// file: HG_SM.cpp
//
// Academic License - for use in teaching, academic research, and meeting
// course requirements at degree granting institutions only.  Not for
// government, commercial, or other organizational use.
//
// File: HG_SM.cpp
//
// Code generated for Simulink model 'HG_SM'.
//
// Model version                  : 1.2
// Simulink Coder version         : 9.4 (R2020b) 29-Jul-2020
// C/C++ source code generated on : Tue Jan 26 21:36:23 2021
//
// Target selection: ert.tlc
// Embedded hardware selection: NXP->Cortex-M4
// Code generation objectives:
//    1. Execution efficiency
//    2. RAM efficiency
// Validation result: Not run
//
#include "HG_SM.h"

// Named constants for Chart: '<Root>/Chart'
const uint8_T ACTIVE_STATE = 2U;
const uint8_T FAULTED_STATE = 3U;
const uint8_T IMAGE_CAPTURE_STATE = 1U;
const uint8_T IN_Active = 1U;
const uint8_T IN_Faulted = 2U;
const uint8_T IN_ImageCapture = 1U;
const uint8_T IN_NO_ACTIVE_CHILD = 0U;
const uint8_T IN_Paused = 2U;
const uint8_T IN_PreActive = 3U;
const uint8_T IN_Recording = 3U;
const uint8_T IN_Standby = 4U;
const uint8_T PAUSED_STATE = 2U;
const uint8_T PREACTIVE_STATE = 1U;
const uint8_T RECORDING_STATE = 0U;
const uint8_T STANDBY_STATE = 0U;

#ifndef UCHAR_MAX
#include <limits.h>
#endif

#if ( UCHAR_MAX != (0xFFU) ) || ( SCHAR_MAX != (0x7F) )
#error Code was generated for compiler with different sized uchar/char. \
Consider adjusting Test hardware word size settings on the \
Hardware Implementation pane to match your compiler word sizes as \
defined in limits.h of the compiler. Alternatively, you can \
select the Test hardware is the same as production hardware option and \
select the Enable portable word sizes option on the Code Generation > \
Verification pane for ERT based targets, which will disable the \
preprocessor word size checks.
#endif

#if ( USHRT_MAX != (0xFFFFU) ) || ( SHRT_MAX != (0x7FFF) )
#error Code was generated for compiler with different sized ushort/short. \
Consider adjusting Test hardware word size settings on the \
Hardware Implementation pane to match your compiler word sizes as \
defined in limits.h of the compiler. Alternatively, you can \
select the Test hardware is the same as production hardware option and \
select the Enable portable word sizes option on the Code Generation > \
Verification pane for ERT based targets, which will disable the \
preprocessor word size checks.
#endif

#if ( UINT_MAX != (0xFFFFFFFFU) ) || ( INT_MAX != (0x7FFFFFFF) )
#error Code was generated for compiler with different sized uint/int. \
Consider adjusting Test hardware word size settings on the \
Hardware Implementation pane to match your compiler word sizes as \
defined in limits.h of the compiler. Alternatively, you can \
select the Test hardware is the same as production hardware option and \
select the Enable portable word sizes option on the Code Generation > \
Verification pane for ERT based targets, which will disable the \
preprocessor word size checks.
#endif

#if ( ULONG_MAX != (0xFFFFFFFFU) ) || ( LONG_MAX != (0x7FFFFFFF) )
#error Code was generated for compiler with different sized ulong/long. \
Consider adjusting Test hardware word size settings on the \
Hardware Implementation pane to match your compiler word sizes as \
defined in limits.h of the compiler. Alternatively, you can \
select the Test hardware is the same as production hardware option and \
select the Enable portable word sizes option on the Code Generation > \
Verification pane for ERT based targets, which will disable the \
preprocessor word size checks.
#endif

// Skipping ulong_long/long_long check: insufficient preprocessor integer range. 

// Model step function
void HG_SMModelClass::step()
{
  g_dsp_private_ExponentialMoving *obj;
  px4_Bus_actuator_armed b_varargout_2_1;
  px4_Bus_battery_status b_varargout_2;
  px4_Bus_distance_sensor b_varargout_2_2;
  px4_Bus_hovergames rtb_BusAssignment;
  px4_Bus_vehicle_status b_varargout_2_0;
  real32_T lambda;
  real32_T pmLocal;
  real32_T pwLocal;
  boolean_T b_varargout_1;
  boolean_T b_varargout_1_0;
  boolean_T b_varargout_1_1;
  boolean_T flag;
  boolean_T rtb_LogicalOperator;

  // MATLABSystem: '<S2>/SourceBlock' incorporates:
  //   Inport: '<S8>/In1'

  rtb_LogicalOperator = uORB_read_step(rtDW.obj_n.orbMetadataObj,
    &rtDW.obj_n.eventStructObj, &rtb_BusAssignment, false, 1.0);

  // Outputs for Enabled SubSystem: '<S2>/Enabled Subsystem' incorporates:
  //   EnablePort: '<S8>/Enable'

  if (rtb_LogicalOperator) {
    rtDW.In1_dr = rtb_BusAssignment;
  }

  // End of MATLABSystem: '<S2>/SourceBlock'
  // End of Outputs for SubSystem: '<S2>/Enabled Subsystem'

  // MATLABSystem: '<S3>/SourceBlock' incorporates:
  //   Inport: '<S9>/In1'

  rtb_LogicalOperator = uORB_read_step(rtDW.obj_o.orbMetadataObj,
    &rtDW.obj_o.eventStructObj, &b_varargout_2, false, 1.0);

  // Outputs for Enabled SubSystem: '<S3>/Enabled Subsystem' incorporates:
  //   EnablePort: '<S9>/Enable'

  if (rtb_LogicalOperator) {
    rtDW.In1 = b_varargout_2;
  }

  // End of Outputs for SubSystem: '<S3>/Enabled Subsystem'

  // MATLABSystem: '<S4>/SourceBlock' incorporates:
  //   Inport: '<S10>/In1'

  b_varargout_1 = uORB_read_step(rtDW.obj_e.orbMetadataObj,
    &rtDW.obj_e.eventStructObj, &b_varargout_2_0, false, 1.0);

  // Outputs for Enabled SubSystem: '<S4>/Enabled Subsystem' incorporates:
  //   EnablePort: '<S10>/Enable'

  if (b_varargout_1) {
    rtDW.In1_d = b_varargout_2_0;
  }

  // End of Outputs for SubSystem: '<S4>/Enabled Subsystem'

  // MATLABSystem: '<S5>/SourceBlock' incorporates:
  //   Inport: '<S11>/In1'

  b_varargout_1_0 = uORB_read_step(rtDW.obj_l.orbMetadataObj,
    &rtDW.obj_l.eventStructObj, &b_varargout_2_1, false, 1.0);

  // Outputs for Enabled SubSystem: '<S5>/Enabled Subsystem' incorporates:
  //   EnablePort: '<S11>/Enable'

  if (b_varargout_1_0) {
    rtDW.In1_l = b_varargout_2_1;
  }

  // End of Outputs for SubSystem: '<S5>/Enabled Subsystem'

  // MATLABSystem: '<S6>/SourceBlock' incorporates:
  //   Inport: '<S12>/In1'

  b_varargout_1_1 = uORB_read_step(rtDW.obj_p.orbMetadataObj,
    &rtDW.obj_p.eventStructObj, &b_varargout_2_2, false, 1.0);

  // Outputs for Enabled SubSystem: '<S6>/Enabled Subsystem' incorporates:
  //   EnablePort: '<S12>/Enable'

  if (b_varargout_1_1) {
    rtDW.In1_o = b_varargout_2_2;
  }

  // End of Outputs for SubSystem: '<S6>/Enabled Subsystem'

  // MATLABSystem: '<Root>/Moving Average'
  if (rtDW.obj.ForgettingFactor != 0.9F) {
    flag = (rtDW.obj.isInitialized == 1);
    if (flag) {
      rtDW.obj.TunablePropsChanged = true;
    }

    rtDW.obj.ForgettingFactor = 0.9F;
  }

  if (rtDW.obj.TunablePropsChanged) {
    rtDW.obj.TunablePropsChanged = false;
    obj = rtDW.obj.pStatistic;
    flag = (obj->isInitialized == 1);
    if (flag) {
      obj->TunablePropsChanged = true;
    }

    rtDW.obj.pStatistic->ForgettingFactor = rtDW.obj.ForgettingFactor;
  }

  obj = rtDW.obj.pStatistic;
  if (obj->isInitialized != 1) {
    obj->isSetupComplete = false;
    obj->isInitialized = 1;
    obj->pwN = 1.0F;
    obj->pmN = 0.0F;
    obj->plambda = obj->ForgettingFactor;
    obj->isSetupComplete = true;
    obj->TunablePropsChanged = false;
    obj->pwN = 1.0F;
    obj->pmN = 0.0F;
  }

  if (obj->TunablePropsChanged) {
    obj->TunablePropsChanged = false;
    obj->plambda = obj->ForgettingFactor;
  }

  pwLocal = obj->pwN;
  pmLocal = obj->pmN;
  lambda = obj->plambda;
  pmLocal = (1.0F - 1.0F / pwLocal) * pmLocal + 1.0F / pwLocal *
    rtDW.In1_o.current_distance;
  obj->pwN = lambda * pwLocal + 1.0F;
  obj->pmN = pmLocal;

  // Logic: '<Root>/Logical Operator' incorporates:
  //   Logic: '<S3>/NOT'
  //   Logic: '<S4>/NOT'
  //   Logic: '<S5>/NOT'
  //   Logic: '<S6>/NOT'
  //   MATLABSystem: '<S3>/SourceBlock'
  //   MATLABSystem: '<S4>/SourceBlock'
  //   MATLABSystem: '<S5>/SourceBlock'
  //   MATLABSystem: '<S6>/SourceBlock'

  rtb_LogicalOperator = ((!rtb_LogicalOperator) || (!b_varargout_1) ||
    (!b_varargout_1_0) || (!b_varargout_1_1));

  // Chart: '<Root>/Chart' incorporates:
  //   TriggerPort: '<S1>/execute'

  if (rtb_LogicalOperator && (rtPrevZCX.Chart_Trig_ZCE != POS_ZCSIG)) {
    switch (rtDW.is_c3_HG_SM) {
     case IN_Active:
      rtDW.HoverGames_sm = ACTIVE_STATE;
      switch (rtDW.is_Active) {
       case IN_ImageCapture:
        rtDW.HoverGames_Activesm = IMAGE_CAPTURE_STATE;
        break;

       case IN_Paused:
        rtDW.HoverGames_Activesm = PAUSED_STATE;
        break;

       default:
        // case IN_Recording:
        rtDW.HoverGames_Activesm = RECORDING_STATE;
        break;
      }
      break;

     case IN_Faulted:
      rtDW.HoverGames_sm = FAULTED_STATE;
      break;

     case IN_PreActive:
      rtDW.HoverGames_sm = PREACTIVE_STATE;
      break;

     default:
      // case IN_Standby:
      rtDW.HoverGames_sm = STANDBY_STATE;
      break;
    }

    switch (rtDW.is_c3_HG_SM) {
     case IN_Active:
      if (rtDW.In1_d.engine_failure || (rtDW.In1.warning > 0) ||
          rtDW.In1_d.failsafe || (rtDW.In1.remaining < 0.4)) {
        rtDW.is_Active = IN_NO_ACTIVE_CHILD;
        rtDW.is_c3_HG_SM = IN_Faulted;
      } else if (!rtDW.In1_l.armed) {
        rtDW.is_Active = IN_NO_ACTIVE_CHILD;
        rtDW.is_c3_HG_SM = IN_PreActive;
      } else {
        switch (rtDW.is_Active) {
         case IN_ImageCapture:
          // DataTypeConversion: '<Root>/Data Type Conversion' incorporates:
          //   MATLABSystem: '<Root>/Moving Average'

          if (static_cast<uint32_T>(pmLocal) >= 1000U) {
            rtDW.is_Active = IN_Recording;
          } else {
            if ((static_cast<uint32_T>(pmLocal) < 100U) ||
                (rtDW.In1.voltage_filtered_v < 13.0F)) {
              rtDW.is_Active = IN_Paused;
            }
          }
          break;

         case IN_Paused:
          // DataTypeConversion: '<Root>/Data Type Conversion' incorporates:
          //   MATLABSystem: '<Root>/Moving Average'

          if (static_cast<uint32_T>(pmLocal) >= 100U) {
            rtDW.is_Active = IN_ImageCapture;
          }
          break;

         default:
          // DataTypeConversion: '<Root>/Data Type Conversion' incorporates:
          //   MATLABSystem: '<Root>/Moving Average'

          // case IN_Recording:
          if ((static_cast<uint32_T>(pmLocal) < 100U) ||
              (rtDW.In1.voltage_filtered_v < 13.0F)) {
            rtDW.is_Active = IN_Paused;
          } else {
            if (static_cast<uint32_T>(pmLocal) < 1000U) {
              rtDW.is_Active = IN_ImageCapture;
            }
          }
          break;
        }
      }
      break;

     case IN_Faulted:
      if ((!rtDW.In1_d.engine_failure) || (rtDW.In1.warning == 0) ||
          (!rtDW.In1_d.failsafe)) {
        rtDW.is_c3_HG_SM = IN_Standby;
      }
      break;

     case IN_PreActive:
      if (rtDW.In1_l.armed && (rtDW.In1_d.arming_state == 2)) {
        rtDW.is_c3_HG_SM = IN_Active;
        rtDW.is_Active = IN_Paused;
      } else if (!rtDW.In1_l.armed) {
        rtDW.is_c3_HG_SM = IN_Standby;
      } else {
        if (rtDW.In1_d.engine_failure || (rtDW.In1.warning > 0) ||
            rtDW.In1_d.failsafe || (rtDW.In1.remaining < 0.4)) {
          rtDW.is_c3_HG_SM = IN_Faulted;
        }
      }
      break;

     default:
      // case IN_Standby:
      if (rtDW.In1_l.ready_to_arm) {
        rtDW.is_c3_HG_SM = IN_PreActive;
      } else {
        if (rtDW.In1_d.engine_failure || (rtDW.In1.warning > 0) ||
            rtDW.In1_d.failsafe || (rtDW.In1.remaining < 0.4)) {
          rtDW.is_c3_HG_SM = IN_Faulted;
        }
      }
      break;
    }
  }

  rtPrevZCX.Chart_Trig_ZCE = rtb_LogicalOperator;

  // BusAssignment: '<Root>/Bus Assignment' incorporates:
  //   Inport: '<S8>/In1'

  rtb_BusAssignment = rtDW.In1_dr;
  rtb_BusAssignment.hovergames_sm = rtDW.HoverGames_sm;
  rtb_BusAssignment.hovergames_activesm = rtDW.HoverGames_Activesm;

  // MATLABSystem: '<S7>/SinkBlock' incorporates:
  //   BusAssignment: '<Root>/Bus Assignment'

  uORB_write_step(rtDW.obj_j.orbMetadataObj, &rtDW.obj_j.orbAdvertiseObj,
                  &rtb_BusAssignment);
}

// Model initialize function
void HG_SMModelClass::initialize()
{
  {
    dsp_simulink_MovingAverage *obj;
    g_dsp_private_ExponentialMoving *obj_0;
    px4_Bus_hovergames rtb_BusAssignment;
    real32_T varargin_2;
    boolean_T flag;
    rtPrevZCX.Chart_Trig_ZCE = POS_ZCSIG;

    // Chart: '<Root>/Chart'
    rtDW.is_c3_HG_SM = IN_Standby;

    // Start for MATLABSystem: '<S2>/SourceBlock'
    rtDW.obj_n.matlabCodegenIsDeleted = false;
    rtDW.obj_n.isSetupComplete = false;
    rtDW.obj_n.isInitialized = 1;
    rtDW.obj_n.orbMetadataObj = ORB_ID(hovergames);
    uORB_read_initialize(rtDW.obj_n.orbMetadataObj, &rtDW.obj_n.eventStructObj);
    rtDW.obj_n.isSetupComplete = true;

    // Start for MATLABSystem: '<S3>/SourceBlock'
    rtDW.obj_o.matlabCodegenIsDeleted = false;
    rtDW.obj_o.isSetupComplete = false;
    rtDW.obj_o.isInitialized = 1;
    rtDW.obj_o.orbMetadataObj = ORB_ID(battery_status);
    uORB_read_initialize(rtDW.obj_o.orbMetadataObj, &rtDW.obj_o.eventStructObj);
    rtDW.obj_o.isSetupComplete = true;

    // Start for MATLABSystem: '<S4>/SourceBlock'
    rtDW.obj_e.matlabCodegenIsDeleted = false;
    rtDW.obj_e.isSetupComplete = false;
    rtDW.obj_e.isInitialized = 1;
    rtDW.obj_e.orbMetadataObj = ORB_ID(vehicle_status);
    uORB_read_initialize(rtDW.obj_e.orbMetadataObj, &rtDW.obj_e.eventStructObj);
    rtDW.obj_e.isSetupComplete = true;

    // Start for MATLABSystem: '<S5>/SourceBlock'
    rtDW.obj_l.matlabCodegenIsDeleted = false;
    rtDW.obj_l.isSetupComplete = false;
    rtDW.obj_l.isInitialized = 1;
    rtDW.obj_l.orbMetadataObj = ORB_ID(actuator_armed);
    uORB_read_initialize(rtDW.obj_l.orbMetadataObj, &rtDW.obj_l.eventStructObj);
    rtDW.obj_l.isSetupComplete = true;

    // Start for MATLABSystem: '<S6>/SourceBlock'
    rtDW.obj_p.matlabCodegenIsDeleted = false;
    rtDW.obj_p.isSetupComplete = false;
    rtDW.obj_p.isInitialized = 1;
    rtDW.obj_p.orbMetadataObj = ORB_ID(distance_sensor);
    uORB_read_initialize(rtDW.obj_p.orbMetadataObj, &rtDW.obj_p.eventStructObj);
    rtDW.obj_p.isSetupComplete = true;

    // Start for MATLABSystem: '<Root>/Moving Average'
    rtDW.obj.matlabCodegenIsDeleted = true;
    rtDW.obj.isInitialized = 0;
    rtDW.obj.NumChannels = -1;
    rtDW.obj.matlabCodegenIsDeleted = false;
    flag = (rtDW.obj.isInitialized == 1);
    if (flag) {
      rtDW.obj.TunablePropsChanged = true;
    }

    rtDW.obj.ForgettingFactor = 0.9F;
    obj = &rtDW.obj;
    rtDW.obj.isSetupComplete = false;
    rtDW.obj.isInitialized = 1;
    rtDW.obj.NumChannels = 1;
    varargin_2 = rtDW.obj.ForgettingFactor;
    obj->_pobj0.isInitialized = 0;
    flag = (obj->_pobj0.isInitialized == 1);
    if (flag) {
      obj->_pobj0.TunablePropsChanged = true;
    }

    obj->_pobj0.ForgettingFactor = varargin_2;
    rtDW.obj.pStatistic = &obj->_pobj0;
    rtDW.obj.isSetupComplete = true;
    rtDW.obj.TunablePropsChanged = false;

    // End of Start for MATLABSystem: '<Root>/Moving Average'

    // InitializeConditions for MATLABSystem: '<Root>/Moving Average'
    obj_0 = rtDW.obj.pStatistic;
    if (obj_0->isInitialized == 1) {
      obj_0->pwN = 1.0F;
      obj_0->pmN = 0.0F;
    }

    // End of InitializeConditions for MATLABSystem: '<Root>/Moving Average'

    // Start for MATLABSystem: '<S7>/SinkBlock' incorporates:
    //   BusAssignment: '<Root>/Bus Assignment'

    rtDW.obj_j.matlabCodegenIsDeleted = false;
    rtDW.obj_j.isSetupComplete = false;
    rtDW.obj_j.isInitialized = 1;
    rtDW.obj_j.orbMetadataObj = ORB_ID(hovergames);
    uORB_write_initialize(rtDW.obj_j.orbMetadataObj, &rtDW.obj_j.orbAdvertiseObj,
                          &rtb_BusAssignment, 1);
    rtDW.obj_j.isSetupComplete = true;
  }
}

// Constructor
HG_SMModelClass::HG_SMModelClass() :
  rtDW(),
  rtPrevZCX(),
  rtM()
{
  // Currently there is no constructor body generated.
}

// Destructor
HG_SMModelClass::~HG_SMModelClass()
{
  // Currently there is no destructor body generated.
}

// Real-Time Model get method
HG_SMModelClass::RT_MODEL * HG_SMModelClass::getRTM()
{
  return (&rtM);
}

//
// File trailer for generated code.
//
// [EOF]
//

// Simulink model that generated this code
simulink model "HG_SM"  (R2020b)
settings: Solver=FixedStepDiscrete  StartTime=0.0  StopTime=10.0  FixedStep=0.1  RelTol=1e-3
undefined symbols (not defined in the file): hovergames_activesm, hovergames_sm
libraries: px4uORBlib x6, dspstat3 x1

== system HG_SM ==
  Bus Assignment : BusAssignment  AssignedSignals=hovergames_sm,hovergames_activesm
  Bus Selector : BusSelector  OutputSignals=voltage_filtered_v,warning,remaining
  Bus Selector1 : BusSelector  OutputSignals=arming_state,engine_failure,failsafe
  Bus Selector2 : BusSelector  OutputSignals=armed,ready_to_arm
  Bus Selector3 : BusSelector  OutputSignals=current_distance
  Chart : Stateflow chart  TreatAsAtomicUnit=on
  Data Type Conversion : DataTypeConversion  OutDataTypeStr=uint32
  Logical Operator : Logic  Operator=OR  Inputs=4  AllPortsSameDT=off  OutDataTypeStr=boolean
  Moving Average : dspstat3/Moving Average  Method=Exponential weighting  ForgettingFactorPort=off  SpecifyWindowLength=on  WindowLength=4  ForgettingFactor=0.9  SimulateUsing=Code generation
  PX4 uORB Read : px4uORBlib/PX4 uORB Read  uORBTopic=hovergames  selectInstance=hovergames  SampleTime=0.1  BlockingMode=off  BlockTimeout=1e-3
  PX4 uORB Read1 : px4uORBlib/PX4 uORB Read  uORBTopic=battery_status  selectInstance=battery_status  SampleTime=0.1  BlockingMode=off  BlockTimeout=1e-3
  PX4 uORB Read2 : px4uORBlib/PX4 uORB Read  uORBTopic=vehicle_status  selectInstance=vehicle_status  SampleTime=0.1  BlockingMode=off  BlockTimeout=1e-3
  PX4 uORB Read3 : px4uORBlib/PX4 uORB Read  uORBTopic=actuator_armed  selectInstance=actuator_armed  SampleTime=0.1  BlockingMode=off  BlockTimeout=1e-3
  PX4 uORB Read4 : px4uORBlib/PX4 uORB Read  uORBTopic=distance_sensor  selectInstance=distance_sensor  SampleTime=0.1  BlockingMode=off  BlockTimeout=1e-3
  PX4 uORB Write : px4uORBlib/PX4 uORB Write  uORBTopic=hovergames  selectInstance=hovergames  MessageQueueLen=1
  Terminator : Terminator
  wires:
  Bus Selector1/1 -> Chart/4(armingState)  "<arming_state>"
  Bus Selector/1 -> Chart/1(voltage)  "<voltage_filtered_v>"
  PX4 uORB Read4/2 -> Bus Selector3/1
  PX4 uORB Read3/2 -> Bus Selector2/1
  PX4 uORB Read/1 -> Terminator/1
  Bus Selector/3 -> Chart/3(batteryRemaining)  "<remaining>"
  PX4 uORB Read2/2 -> Bus Selector1/1
  Bus Selector2/1 -> Chart/7(isArmed)  "<armed>"
  PX4 uORB Read1/2 -> Bus Selector/1
  Bus Selector1/3 -> Chart/6(failSafe)  "<failsafe>"
  Bus Selector/2 -> Chart/2(batteryWarning)  "<warning>"
  Bus Selector3/1 -> Moving Average/1  "<current_distance>"
  Bus Selector1/2 -> Chart/5(engineFailure)  "<engine_failure>"
  Bus Selector2/2 -> Chart/8(isReadyToArm)  "<ready_to_arm>"
  Bus Assignment/1 -> PX4 uORB Write/1
  PX4 uORB Read/2 -> Bus Assignment/1
  Chart/1(HoverGames_sm) -> Bus Assignment/2
  Chart/2(HoverGames_Activesm) -> Bus Assignment/3
  Logical Operator/1 -> Chart/Trigger
  PX4 uORB Read1/1 -> Logical Operator/1
  PX4 uORB Read2/1 -> Logical Operator/2
  PX4 uORB Read3/1 -> Logical Operator/3
  PX4 uORB Read4/1 -> Logical Operator/4
  Data Type Conversion/1 -> Chart/9(currentDistance)
  Moving Average/1 -> Data Type Conversion/1

== stateflow chart HG_SM/Chart ==
  settings: stateMachineType=MOORE_MACHINE
  state Faulted
    HoverGames_sm = FAULTED_STATE;
  state Standby
    HoverGames_sm = STANDBY_STATE;
  state Active
    HoverGames_sm = ACTIVE_STATE;
    state Recording
      HoverGames_Activesm = RECORDING_STATE
    state Paused
      HoverGames_Activesm = PAUSED_STATE;
    state ImageCapture
      HoverGames_Activesm = IMAGE_CAPTURE_STATE
    (default) -> Paused
    Recording -> Paused [order 1] : [currentDistance <  100 || voltage < 13]
    Paused -> ImageCapture : [currentDistance >= 100]
    ImageCapture -> Paused [order 2] : [currentDistance <  100 || voltage < 13]
    ImageCapture -> Recording [order 1] : [currentDistance >= 1000]
    Recording -> ImageCapture [order 2] : [currentDistance < 1000]
  state PreActive
    HoverGames_sm = PREACTIVE_STATE;
  Faulted -> Standby : [engineFailure ==false || batteryWarning == 0 || failSafe == false]
  (default) -> Standby
  Standby -> Faulted [order 2] : [engineFailure == true || batteryWarning > 0 || failSafe == true||  batteryRemaining < 0.4]
  PreActive -> Faulted [order 3] : [engineFailure == true || batteryWarning > 0 || failSafe == true || batteryRemaining < 0.4]
  Active -> Faulted [order 1] : [engineFailure == true || batteryWarning > 0 || failSafe == true || batteryRemaining < 0.4]
  Standby -> PreActive [order 1] : [isReadyToArm==true]
  PreActive -> Standby [order 2] : [isArmed == false]
  Active -> PreActive [order 2] : [isArmed == false]
  PreActive -> Active [order 1] : [isArmed == true && armingState== ARMING_STATE_ARMED]
  data: voltage input single; batteryWarning input uint8; batteryRemaining input; armingState input uint8; engineFailure input boolean; failSafe input boolean; isArmed input boolean; isReadyToArm input boolean; currentDistance input uint32; HoverGames_sm output uint8; HoverGames_Activesm output uint8; STANDBY_STATE constant uint8 =0; PREACTIVE_STATE constant uint8 =1; ACTIVE_STATE constant uint8 =2; FAULTED_STATE constant uint8 =3; RECORDING_STATE constant uint8 =0; IMAGE_CAPTURE_STATE constant uint8 =1; PAUSED_STATE constant uint8 =2; ARMING_STATE_ARMED constant uint8 =2
  events: execute input RISING_EDGE_EVENT
